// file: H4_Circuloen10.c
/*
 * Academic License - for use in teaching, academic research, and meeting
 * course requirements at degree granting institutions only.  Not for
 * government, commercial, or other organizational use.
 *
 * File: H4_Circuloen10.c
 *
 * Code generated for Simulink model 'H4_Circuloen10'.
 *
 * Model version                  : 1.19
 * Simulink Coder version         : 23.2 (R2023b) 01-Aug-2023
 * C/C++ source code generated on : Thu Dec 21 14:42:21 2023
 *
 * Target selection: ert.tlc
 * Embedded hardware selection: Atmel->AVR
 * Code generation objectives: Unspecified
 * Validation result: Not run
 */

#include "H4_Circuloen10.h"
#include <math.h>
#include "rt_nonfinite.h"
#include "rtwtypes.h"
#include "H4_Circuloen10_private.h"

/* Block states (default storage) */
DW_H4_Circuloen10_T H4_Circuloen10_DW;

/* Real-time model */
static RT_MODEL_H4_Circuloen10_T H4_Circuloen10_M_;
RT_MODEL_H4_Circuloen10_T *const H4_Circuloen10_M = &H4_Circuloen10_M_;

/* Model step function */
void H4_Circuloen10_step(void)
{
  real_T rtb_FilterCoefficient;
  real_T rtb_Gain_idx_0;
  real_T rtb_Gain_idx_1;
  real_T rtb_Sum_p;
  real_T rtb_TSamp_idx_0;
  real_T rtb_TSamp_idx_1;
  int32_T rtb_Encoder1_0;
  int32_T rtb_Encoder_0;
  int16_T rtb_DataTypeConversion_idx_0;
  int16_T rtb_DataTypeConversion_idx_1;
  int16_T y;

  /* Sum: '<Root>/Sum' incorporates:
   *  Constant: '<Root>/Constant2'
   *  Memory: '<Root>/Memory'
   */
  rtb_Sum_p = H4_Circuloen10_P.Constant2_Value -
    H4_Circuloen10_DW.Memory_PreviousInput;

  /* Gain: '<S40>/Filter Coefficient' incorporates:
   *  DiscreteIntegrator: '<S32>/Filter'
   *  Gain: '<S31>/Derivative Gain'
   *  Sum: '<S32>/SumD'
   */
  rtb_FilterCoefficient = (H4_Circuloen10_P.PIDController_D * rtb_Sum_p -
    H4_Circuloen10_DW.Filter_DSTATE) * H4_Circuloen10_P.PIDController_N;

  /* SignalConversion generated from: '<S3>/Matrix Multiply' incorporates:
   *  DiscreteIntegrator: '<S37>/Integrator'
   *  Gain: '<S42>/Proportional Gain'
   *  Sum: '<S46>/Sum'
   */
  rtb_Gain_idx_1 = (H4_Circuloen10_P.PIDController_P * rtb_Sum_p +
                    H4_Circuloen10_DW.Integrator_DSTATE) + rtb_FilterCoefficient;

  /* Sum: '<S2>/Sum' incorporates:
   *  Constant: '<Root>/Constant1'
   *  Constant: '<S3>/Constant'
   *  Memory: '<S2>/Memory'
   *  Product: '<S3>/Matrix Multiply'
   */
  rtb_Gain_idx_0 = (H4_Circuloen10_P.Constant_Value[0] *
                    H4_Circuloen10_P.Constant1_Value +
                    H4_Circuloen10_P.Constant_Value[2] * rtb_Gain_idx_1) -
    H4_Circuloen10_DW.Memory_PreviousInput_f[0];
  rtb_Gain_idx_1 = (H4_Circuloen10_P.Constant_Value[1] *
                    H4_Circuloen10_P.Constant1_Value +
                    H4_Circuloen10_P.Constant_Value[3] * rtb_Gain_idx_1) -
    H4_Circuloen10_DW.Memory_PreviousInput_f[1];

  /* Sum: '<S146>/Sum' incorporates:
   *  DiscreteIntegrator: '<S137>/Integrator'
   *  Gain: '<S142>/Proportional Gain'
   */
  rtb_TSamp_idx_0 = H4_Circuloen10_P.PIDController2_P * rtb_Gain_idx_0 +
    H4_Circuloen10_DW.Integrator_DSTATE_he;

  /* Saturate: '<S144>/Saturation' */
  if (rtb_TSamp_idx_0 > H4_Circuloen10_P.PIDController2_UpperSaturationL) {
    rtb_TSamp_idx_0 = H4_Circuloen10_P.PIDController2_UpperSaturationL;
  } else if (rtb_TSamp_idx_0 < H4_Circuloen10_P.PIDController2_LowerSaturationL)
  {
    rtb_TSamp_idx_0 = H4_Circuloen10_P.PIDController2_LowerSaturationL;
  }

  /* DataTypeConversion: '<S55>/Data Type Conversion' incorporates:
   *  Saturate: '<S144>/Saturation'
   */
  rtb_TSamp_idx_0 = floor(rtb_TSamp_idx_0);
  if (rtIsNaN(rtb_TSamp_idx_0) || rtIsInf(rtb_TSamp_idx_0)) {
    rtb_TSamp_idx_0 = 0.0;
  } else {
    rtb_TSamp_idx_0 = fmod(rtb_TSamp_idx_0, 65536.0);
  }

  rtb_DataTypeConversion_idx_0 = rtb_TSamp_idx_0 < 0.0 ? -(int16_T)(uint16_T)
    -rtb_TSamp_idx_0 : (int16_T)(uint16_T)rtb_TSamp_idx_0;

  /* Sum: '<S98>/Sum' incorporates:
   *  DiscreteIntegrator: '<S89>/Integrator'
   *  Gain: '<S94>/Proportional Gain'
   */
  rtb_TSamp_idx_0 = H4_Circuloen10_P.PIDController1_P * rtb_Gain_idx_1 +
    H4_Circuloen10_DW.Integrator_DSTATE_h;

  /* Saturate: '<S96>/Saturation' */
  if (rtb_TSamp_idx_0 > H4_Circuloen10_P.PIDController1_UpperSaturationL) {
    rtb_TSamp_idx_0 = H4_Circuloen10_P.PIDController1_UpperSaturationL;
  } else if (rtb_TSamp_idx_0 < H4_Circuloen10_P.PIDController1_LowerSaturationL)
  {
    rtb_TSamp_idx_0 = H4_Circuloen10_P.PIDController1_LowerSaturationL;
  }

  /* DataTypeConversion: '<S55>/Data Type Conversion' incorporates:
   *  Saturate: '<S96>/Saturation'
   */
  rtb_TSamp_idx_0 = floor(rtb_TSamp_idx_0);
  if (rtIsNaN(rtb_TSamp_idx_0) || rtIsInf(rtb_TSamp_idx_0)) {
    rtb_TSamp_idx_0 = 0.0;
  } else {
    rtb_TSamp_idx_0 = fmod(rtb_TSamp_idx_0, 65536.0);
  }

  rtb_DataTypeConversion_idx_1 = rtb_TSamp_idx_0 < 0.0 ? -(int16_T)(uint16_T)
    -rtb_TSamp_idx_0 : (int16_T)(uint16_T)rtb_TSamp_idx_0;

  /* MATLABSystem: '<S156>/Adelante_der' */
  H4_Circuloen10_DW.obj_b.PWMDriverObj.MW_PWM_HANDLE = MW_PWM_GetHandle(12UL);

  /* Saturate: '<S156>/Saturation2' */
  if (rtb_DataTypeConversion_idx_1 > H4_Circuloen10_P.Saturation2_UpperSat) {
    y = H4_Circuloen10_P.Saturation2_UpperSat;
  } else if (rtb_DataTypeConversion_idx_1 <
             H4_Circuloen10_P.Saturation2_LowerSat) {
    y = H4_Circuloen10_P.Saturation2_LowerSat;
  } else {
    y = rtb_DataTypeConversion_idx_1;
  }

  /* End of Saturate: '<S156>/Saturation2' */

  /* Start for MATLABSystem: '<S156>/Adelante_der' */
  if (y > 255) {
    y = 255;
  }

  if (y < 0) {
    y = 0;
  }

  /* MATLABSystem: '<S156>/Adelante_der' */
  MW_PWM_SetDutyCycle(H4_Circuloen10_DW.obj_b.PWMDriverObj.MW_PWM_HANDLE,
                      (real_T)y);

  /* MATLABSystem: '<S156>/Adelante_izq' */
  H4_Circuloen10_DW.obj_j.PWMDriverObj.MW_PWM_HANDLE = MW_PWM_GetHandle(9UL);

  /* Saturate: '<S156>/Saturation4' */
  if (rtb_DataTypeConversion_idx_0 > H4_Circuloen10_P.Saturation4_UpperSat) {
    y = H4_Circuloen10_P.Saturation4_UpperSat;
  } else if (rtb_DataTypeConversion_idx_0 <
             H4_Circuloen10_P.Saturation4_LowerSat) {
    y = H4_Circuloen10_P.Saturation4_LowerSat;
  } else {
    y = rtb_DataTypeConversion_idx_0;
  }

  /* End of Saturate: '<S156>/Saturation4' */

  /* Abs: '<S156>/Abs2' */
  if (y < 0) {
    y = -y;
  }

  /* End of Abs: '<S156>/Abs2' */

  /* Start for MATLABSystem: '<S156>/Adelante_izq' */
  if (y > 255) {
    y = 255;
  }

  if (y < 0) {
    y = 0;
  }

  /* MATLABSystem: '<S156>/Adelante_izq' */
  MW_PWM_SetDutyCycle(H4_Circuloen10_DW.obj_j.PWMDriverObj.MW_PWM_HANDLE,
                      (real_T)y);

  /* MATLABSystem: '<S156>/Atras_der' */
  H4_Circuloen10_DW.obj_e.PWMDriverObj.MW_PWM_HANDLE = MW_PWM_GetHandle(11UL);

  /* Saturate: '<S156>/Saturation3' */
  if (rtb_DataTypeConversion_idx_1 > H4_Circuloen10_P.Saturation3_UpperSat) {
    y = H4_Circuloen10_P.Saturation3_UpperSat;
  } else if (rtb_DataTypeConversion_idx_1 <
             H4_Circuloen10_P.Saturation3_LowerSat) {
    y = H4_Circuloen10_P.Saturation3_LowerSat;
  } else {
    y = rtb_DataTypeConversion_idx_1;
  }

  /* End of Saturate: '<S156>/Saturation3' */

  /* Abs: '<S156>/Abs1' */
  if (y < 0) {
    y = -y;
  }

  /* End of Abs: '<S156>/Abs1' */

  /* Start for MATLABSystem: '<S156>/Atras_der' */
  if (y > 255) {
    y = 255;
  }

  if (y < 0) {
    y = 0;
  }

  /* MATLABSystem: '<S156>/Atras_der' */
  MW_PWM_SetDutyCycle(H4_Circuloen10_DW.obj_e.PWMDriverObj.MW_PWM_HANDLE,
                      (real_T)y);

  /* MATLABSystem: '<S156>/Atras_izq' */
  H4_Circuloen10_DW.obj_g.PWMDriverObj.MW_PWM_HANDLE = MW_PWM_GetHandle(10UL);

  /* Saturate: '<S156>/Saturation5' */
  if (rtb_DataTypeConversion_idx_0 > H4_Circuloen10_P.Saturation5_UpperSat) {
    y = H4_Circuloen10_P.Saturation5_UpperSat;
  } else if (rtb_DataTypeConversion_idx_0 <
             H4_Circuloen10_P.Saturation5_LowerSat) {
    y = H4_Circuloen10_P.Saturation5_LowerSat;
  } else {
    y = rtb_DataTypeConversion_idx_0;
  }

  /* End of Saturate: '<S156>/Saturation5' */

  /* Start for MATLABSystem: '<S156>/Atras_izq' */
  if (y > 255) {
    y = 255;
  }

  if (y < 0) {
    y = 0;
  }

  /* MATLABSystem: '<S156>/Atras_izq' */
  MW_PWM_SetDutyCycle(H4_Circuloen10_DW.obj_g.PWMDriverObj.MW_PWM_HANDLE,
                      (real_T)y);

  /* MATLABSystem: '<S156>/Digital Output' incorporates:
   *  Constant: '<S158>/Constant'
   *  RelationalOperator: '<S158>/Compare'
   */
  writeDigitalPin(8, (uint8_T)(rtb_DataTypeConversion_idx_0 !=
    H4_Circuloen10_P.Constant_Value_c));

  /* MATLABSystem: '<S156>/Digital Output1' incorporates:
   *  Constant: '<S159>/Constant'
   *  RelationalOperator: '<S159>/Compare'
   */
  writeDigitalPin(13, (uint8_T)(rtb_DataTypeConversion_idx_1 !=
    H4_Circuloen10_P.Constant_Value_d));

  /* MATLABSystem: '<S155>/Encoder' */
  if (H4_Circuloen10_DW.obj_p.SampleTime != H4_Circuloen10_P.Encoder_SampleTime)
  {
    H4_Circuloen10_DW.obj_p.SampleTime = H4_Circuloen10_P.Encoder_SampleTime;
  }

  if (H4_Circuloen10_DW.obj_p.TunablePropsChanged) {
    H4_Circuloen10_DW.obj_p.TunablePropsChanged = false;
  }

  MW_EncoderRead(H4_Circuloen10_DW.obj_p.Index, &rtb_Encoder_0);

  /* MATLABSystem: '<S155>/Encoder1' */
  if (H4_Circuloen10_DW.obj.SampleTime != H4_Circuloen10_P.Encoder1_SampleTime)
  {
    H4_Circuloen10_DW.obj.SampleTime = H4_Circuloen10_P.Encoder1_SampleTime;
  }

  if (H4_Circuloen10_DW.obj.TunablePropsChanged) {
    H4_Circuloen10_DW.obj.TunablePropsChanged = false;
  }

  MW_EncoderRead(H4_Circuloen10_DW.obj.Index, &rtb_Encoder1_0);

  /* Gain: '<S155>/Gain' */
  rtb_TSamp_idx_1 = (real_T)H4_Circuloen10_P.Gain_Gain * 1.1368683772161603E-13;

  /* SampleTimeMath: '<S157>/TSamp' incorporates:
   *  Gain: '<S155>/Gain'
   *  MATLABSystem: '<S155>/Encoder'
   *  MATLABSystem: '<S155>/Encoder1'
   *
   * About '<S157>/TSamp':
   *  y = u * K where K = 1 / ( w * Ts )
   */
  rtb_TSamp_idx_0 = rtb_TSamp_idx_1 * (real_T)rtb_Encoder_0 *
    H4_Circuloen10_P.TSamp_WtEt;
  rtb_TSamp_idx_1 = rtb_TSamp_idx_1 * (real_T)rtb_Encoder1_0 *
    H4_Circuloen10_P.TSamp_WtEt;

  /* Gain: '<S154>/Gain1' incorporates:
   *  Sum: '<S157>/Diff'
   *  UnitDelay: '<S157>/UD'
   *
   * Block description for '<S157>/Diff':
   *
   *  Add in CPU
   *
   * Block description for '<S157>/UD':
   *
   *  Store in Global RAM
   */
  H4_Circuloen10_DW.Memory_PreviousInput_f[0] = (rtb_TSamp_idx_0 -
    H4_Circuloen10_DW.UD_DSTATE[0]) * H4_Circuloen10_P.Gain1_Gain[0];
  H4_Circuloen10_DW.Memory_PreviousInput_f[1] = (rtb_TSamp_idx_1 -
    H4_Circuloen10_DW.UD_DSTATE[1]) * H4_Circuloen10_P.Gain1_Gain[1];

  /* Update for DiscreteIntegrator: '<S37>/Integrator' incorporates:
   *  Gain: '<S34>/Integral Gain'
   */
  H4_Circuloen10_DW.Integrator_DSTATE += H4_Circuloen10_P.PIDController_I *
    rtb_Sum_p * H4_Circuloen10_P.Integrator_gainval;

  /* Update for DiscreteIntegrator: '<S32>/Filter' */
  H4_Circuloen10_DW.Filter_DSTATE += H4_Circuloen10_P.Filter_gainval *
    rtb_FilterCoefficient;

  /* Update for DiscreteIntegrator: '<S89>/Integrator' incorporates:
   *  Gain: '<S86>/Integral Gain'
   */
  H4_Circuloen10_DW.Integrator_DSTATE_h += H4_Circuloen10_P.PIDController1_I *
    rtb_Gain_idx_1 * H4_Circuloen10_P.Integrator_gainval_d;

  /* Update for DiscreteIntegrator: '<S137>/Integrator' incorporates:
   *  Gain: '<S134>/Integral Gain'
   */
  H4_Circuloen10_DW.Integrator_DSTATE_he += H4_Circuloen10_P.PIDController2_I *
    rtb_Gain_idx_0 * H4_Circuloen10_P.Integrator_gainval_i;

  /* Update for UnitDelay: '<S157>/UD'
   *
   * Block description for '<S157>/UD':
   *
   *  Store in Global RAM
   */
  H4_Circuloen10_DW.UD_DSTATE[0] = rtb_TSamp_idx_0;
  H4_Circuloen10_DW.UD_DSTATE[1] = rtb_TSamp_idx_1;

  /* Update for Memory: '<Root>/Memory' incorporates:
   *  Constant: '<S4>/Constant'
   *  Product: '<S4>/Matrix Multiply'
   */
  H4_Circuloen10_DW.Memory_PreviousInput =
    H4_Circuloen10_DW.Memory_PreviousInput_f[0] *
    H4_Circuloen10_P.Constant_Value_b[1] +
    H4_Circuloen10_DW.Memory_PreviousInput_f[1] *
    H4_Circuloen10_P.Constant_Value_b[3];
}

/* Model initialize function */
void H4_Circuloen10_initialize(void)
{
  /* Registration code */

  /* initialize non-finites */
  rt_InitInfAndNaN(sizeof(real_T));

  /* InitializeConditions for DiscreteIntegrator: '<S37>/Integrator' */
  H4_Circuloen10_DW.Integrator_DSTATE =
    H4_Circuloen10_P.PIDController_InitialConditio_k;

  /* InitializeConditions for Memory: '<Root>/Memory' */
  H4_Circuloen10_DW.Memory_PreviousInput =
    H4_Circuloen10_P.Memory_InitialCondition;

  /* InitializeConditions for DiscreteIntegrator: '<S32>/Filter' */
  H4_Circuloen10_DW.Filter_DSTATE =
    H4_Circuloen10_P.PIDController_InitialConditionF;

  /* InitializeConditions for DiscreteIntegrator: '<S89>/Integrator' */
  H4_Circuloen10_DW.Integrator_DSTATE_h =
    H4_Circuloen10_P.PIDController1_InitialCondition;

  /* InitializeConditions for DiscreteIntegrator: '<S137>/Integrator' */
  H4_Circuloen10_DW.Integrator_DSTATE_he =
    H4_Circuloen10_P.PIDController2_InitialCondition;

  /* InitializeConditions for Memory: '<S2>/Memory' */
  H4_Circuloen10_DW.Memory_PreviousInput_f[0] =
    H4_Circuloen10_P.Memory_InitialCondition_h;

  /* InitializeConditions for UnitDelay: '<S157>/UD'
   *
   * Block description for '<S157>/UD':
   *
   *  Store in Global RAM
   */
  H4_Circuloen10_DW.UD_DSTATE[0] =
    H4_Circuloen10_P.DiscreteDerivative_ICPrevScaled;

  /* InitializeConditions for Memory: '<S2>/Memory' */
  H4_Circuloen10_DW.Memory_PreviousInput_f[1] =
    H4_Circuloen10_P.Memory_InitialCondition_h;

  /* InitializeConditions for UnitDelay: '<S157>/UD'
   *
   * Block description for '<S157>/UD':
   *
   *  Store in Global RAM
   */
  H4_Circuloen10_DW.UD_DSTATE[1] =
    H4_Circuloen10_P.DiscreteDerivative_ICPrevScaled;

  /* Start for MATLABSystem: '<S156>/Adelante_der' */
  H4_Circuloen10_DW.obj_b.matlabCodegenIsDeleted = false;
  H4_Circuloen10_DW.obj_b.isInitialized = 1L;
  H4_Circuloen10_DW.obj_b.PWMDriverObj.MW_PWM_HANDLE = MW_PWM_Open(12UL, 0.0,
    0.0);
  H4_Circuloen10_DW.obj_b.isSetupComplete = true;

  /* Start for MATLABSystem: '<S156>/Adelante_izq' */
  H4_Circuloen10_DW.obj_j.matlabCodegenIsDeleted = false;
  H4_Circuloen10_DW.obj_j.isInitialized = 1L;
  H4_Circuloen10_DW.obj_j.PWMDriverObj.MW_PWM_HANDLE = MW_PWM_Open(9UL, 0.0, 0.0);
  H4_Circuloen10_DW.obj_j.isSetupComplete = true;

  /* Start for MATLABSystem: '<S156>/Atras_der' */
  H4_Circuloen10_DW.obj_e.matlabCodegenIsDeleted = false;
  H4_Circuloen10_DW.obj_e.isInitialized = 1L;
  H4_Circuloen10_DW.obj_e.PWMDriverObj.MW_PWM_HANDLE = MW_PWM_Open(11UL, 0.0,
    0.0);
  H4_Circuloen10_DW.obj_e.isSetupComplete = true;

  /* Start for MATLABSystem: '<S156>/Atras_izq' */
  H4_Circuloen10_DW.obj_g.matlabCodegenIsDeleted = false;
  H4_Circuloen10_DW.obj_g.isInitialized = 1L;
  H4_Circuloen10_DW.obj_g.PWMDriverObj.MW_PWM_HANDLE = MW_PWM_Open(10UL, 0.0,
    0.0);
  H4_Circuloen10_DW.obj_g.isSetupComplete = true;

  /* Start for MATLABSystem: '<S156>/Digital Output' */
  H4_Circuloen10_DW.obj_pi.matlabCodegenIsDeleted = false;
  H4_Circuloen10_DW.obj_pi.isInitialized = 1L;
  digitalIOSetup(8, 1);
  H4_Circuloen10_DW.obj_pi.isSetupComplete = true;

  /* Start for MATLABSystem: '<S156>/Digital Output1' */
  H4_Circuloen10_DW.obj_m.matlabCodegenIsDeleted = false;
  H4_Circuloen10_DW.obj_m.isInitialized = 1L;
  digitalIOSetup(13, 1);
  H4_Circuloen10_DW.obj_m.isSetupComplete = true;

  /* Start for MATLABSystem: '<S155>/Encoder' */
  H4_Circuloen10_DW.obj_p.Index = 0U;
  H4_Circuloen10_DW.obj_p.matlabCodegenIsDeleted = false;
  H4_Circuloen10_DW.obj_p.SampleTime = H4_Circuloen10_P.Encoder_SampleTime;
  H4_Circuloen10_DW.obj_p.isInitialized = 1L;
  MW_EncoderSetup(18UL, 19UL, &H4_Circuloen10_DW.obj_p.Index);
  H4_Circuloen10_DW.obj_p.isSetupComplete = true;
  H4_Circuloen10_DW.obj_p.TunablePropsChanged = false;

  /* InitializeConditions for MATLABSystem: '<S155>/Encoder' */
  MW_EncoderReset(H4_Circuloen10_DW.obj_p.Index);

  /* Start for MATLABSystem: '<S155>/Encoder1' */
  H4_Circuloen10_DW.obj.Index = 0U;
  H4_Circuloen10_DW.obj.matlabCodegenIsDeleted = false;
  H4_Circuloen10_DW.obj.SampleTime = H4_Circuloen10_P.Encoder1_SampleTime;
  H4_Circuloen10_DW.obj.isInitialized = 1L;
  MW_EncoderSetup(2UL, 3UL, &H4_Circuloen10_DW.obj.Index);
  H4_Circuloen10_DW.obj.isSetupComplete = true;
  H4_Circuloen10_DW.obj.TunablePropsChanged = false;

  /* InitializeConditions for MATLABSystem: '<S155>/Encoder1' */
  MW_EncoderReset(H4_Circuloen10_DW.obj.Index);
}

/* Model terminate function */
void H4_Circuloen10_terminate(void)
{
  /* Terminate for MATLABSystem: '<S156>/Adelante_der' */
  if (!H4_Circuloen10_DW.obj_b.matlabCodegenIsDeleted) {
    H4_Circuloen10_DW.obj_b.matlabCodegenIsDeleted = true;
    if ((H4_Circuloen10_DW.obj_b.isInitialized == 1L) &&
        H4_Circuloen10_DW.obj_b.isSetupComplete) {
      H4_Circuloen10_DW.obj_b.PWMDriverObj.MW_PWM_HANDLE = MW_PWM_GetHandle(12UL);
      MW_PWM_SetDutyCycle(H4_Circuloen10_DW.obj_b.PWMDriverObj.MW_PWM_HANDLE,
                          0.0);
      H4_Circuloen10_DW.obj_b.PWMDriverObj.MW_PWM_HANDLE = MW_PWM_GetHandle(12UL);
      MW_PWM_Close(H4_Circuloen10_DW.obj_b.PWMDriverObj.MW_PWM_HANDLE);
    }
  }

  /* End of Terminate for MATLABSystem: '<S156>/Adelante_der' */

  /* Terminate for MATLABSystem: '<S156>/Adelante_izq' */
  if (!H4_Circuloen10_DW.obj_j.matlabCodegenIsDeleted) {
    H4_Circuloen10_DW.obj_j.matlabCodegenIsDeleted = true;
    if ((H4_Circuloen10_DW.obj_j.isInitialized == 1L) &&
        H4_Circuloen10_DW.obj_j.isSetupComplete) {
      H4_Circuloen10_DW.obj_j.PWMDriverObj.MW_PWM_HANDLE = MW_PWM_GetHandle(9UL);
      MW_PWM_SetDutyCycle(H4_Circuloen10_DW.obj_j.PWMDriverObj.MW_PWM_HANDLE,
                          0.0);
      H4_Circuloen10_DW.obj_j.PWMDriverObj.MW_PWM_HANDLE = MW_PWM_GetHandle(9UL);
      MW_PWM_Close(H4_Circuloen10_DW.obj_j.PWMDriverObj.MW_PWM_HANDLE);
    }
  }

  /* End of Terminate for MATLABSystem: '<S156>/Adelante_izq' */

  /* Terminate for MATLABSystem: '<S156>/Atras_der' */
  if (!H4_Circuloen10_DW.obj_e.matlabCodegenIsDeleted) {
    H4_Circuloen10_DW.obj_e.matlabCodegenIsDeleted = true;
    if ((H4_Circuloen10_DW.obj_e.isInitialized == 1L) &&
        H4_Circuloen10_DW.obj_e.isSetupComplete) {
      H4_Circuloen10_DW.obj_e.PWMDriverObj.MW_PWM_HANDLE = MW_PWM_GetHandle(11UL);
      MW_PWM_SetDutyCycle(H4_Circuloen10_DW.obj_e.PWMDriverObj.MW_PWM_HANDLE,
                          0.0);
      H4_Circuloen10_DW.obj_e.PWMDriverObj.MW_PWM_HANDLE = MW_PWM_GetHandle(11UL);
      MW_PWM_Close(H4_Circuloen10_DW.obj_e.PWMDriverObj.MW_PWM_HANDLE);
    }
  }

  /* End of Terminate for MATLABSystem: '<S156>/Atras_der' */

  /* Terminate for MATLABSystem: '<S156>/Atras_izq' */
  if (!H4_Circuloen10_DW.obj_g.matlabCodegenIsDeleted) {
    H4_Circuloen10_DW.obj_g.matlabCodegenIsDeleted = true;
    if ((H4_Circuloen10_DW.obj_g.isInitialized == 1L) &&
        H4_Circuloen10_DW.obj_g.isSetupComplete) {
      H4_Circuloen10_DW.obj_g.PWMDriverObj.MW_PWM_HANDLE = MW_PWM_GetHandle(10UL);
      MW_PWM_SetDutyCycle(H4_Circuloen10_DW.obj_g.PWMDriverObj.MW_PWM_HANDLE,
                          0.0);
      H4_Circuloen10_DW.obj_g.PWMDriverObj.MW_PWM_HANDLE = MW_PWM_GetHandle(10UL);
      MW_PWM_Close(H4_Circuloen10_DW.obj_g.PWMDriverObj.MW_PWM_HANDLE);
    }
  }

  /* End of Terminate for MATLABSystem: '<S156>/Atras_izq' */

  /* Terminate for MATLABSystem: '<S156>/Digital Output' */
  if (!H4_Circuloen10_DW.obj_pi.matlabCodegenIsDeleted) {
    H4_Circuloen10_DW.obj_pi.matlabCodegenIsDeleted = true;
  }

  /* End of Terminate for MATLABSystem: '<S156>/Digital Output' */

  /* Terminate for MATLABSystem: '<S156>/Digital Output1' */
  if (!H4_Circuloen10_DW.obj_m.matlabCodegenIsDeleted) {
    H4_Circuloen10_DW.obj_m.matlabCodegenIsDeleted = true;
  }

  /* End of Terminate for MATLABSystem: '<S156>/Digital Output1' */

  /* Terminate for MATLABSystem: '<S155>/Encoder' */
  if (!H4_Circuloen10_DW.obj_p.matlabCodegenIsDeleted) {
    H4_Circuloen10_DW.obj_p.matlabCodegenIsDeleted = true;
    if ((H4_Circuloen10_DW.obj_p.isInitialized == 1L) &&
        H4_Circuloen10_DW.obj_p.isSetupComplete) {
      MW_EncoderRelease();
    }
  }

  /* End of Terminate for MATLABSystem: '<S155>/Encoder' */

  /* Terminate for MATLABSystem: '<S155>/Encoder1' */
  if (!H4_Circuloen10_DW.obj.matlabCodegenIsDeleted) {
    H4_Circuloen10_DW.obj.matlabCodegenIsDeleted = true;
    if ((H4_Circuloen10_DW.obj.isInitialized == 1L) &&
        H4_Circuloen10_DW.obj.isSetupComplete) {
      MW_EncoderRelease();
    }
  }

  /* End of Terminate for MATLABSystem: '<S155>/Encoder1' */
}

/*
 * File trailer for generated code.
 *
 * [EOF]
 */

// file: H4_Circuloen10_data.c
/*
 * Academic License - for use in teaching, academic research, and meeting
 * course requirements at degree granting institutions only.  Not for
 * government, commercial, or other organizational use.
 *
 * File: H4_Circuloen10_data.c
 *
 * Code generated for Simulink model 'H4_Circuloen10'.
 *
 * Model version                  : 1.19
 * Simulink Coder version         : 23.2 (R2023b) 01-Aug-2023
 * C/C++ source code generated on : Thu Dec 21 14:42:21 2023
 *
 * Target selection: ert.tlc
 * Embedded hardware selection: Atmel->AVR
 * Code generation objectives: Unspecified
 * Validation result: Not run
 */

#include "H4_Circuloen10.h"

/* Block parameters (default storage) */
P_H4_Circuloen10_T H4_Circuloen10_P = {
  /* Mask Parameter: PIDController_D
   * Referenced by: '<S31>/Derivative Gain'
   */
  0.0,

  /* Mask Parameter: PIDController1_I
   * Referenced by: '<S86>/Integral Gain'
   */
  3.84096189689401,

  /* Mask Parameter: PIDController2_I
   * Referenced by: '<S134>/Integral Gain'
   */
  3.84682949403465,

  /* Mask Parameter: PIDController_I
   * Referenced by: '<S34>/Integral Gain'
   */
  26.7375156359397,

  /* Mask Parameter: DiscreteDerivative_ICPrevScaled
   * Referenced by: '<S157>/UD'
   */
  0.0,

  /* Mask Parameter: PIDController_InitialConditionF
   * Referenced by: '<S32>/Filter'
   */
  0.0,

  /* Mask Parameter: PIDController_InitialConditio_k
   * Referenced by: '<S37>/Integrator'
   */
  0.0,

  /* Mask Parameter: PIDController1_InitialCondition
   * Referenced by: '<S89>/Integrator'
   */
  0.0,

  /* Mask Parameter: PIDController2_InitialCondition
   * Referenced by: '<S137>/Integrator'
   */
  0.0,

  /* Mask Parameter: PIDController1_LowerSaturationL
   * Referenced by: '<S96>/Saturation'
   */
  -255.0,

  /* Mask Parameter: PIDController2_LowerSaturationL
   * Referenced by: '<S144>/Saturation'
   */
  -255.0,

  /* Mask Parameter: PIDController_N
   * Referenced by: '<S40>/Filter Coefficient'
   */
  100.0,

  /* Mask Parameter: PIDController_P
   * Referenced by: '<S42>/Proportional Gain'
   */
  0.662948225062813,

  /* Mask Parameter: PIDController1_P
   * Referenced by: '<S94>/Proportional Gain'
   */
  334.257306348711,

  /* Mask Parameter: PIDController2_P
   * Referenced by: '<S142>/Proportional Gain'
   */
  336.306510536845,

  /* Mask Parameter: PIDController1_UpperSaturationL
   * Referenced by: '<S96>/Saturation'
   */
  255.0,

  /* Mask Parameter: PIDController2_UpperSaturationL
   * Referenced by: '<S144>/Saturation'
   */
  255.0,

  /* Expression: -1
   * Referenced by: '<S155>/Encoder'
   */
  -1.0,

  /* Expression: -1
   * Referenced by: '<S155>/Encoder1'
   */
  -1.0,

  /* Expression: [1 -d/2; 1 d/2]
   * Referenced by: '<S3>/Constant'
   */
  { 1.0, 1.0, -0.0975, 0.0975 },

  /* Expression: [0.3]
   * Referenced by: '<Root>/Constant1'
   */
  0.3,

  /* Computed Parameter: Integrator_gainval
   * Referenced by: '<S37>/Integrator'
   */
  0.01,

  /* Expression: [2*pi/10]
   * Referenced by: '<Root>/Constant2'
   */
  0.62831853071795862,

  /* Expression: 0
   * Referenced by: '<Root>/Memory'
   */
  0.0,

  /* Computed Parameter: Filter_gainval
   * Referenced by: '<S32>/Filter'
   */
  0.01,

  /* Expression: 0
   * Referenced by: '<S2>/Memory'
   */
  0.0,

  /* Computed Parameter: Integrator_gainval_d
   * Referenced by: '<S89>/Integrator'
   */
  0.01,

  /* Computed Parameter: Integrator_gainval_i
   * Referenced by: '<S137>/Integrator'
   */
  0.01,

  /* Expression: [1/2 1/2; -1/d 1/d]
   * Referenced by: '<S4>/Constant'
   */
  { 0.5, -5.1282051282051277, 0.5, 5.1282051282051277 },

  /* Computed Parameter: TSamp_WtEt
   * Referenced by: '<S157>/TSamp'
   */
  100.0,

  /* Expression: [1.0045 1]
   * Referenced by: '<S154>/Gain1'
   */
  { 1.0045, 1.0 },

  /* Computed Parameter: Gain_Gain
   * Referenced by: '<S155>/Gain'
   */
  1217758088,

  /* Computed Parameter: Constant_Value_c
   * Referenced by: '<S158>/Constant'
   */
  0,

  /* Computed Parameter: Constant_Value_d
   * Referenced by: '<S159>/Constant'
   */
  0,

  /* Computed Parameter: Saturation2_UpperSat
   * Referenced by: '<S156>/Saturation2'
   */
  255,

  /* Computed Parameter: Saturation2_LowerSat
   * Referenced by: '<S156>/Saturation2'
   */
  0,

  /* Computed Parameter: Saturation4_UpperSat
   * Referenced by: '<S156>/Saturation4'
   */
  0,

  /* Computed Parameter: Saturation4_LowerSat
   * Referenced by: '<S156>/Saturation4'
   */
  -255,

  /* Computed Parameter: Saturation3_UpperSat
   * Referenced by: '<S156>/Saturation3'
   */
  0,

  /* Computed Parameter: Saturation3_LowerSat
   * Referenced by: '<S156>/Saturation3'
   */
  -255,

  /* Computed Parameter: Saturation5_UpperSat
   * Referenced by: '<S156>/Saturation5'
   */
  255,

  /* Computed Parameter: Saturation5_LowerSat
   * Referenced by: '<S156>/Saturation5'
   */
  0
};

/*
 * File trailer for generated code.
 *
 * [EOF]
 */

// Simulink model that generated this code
simulink model "H4_Circuloen10"  (R2023b)
settings: Solver=FixedStepDiscrete  StartTime=0.0  StopTime=10  FixedStep=0.01  RelTol=1e-3  EnableMultiTasking=on
model workspace (MAT data in the model file):
  d = 0.195
libraries: slpidlib x1

== system H4_Circuloen10 ==
  Constant1 : Constant  Value=[0.25]
  Constant2 : Constant  Value=[2*pi/10]
  Demux : Demux  Outputs=2
  Memory : Memory
  Mux : Mux  Inputs=2
  PID Controller : slpidlib/PID Controller  Controller=PID  Form=Parallel  TimeDomain=Discrete-time  UseExternalTs=off  SampleTime=-1  IntegratorMethod=Forward Euler  FilterMethod=Forward Euler  ControllerParametersSource=internal  P=0.662948225062813  I=26.7375156359397  UseKiTs=off  D=0  N=100  UseFilter=on  TunerSelectOption=Transfer Function Based (PID Tuner App)  InitialConditionSource=internal  InitialConditionForIntegrator=0  InitialConditionForFilter=0  DifferentiatorICPrevScaledInput=0  ExternalReset=none  TrackingMode=off  Kt=1  LimitOutput=off  SatLimitsSource=internal  UpperSaturationLimit=inf  LowerSaturationLimit=-inf  LinearizeAsGain=on  AntiWindupMode=none  Kb=1  LimitIntegrator=off  UpperIntegratorSaturationLimit=inf  LowerIntegratorSaturationLimit=-inf  POutMin=[]  POutMax=[]  IOutMin=[]  IOutMax=[]  DOutMin=[]  DOutMax=[]  NOutMin=[]  NOutMax=[]  SumOutMin=[]  SumOutMax=[]  SaturationOutMin=[]  SaturationOutMax=[]  PParamMin=[]  PParamMax=[]  IParamMin=[]  IParamMax=[]  DParamMin=[]  DParamMax=[]  NParamMin=[]  NParamMax=[]  KbParamMin=[]  KbParamMax=[]  KtParamMin=[]  KtParamMax=[]  KbOutMin=[]  KbOutMax=[]  KtOutMin=[]  KtOutMax=[]  IntegratorOutMin=[]  IntegratorOutMax=[]  FilterOutMin=[]  FilterOutMax=[]  SumI1OutMin=[]  SumI1OutMax=[]  SumI2OutMin=[]  SumI2OutMax=[]  SumI3OutMin=[]  SumI3OutMax=[]  SumI4OutMin=[]  SumI4OutMax=[]  SumDOutMin=[]  SumDOutMax=[]  DifferentiatorOutMin=[]  DifferentiatorOutMax=[]  FilterDiffOutCoefMin=[]  FilterDiffOutCoefMax=[]  ReciprocalOutMin=[]  ReciprocalOutMax=[]  SumDenOutMin=[]  SumDenOutMax=[]  SumNumOutMin=[]  SumNumOutMax=[]  DivideOutMin=[]  DivideOutMax=[]  UdiffTsProdOutMin=[]  UdiffTsProdOutMax=[]  NTsProdOutMin=[]  NTsProdOutMax=[]  UintegralTsProdOutMin=[]  UintegralTsProdOutMax=[]  UngainTsProdOutMin=[]  UngainTsProdOutMax=[]  ClampingZeroOutDataTypeStr=Inherit: Inherit via back propagation  ClampingZeroOutMin=[]  ClampingZeroOutMax=[]  FilterDenConstantOutDataTypeStr=Inherit: Inherit via back propagation  FilterDenConstantOutMin=[]  FilterDenConstantOutMax=[]  PCopyOutDataTypeStr=Inherit: Inherit via back propagation  PCopyOutMin=[]  PCopyOutMax=[]  NCopyOutDataTypeStr=Inherit: Inherit via back propagation  NCopyOutMin=[]  NCopyOutMax=[]  IntegratorContinuousStateAttributes=''  IntegratorStateMustResolveToSignalObject=off  IntegratorRTWStateStorageClass=Auto  FilterContinuousStateAttributes=''  FilterStateMustResolveToSignalObject=off  FilterRTWStateStorageClass=Auto  ParallelPVariant=InternalParameters  IdealPVariant=Disabled  IVariant=InternalParameters  DVariant=InternalParameters  IntegratorVariant=Discrete  SatVariant=Disabled  AWVariant=Passthrough  PCopyVariant=Disabled  TRVariant=Disabled  FdbkBlocksVariant=Forward  IdealPFdbkVariant=Disabled  SatFdbkVariant=Disabled  DerivativeFilterVariant=ForwardEulerFilter  NVariant=InternalParameters  NCopyVariant=Disabled  FilterICVariant=InternalICsFilter  IntegratorICVariant=InternalICs  ExternalResetVariant=Disabled  TRSumVariant=Passthrough  SumFdbkVariant=Disabled  SumVariant=Sum_PID  TsampFilterVariant=InternalTs  TsampNgainVariant=Passthrough  TsampIntegralVariant=Disabled_SignalSpec  ExternalSaturationOutDataTypeStr=Inherit: Same as second input
  Subsystem Reference : Subsystem  ReferencedSubsystem=Piero_ControladoZ_memoria
  Subsystem Reference1 : Subsystem  ReferencedSubsystem=MCI2
  Subsystem Reference2 : Subsystem  ReferencedSubsystem=MCD2
  Subsystem Reference4 : Subsystem  ReferencedSubsystem=OdometriaZ
  Sum : Sum  Inputs=|+-
  Terminator : Terminator
  wires:
  Subsystem Reference1/1 -> Subsystem Reference/1
  Subsystem Reference2/1 -> Demux/1, Subsystem Reference4/1
  Subsystem Reference/1 -> Subsystem Reference2/1
  PID Controller/1 -> Mux/2  "rel"
  Mux/1 -> Subsystem Reference1/1
  Constant1/1 -> Mux/1
  Sum/1 -> PID Controller/1
  Constant2/1 -> Sum/1
  Demux/1 -> Terminator/1
  Demux/2 -> Memory/1
  Memory/1 -> Sum/2
